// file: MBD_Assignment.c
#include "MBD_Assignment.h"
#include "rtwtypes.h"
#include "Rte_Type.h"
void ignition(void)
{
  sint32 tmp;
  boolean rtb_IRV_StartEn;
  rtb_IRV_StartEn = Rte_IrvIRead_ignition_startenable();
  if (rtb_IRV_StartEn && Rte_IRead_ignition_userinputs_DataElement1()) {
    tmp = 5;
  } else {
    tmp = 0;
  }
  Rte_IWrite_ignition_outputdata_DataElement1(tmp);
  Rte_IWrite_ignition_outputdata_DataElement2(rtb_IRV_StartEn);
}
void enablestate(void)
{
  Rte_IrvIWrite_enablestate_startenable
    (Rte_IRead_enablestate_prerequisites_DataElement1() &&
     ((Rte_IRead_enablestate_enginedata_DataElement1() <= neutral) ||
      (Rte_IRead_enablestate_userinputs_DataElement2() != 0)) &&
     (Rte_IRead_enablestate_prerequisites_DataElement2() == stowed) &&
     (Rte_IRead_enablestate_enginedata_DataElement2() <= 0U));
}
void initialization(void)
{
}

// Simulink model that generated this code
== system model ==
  Inport#1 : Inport
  Inport#2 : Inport
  Inport#3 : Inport
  Inport#4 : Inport
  Inport#5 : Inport
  Inport#6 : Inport
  Inport#7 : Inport
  Inport#8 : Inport
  Outport#1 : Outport  <- 1: Subsystem#1
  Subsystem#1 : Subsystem  <- 1: Subsystem#2, 2: Inport#3, Trigger: Inport#1
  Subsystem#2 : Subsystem  <- 1: Inport#4, 2: Inport#5, 3: Inport#6, 4: Inport#7, 5: Inport#8, Trigger: Inport#2
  Outport#2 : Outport  <- 1: Subsystem#1/2
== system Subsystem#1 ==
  Inport#9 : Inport
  Inport#10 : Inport
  TriggerPort#1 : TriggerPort  TriggerType=function-call
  Outport#3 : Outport  <- 1: Switch#1
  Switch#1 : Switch  Criteria=u2 > Threshold  <- 1: Constant#1, 2: Logic#1, 3: Constant#2
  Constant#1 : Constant  Value=5
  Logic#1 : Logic  <- 1: Inport#9, 2: Inport#10
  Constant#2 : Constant  Value=0
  Outport#4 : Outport  <- 1: Inport#9
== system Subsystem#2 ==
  Inport#11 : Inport
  Inport#12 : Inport
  Inport#13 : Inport
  Inport#14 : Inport
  Inport#15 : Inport
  TriggerPort#2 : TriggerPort  TriggerType=function-call
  Outport#5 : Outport  <- 1: Logic#2
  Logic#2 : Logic  Inputs=4  <- 1: Inport#11, 2: Logic#3, 3: RelationalOperator#1, 4: Logic#4
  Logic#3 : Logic  Operator=OR  <- 1: RelationalOperator#2, 2: CompareToConstant#1
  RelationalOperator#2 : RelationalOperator  Operator=<=  <- 1: Inport#12, 2: Constant#3
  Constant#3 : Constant  Value=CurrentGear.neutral
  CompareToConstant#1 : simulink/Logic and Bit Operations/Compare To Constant  relop=~=  const=0  <- 1: Inport#13
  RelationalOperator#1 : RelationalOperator  Operator===  <- 1: Inport#14, 2: Constant#4
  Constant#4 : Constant  Value=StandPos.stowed
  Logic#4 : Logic  Operator=NOT  <- 1: CompareToConstant#2
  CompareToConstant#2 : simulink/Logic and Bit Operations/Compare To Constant  relop=>  const=0  <- 1: Inport#15
